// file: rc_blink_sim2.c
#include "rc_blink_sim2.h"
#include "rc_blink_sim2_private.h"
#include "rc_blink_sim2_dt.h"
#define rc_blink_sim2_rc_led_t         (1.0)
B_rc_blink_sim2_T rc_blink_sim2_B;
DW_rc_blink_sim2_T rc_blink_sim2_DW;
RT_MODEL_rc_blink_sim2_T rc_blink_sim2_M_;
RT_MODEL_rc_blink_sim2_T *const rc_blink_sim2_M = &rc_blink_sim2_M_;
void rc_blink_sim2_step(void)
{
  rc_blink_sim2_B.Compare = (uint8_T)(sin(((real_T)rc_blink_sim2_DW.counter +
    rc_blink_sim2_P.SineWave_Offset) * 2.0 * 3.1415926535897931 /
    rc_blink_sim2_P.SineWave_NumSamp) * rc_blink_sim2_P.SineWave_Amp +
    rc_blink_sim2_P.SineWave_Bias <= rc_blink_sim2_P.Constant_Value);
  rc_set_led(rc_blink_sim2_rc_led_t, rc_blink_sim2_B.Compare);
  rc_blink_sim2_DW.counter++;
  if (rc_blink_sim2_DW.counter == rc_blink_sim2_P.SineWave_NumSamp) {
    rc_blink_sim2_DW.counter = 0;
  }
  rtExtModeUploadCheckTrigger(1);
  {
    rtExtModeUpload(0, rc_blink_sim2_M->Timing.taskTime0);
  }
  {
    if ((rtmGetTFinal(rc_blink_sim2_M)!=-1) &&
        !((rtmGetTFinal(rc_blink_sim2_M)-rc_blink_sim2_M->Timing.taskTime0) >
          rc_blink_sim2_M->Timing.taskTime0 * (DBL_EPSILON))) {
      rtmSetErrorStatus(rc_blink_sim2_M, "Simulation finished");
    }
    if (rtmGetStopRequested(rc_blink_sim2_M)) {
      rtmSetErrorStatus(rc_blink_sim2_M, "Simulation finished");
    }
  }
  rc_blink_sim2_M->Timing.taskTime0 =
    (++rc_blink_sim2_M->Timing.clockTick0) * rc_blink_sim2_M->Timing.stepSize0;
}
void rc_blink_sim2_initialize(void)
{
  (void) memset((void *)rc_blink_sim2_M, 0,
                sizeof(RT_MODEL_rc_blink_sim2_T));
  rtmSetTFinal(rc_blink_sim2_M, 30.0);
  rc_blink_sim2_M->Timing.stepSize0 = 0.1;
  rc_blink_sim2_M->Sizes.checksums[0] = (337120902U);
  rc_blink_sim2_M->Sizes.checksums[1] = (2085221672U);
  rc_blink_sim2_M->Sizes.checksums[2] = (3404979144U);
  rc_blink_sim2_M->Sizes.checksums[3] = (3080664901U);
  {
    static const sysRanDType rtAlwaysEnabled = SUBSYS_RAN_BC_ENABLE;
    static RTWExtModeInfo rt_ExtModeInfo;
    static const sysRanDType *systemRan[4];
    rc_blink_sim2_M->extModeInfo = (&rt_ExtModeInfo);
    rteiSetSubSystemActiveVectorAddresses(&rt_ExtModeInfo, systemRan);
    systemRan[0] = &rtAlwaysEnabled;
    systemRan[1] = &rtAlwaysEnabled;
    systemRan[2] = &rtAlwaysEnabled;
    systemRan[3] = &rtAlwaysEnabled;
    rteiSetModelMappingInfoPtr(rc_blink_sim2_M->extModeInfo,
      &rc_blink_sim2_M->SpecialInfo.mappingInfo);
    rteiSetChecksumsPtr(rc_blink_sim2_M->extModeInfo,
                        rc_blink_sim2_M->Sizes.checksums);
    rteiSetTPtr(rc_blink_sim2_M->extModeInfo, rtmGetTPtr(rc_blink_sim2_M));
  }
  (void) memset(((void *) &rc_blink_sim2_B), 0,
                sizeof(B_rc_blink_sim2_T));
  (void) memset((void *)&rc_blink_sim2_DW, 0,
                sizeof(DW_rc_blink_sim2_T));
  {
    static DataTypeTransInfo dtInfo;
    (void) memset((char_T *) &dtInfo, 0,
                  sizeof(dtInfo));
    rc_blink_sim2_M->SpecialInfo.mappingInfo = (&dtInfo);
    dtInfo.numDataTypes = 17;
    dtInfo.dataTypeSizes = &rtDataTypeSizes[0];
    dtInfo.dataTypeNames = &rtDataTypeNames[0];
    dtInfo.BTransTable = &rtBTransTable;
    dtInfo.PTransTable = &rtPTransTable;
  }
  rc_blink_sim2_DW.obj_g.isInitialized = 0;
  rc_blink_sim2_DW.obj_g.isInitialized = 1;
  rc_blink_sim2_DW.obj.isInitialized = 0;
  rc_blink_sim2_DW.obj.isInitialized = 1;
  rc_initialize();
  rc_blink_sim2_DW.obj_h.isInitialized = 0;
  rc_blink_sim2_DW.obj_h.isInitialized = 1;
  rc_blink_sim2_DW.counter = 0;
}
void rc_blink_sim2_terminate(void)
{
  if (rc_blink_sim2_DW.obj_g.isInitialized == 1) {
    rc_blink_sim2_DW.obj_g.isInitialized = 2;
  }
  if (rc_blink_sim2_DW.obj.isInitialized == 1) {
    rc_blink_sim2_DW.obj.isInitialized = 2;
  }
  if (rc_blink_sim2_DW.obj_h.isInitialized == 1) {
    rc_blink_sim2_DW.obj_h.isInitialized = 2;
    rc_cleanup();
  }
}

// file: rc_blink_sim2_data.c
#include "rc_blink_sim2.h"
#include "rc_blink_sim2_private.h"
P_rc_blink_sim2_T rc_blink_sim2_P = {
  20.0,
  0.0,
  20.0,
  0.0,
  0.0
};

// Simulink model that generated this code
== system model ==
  MATLABSystem#1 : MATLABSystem  <- 1: CompareToZero#1
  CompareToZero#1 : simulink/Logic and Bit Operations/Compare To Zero  relop=<=  <- 1: SineWave
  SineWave : Sin  Amplitude=20  Frequency=2
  MATLABSystem#2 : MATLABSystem
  MATLABSystem#3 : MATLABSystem
